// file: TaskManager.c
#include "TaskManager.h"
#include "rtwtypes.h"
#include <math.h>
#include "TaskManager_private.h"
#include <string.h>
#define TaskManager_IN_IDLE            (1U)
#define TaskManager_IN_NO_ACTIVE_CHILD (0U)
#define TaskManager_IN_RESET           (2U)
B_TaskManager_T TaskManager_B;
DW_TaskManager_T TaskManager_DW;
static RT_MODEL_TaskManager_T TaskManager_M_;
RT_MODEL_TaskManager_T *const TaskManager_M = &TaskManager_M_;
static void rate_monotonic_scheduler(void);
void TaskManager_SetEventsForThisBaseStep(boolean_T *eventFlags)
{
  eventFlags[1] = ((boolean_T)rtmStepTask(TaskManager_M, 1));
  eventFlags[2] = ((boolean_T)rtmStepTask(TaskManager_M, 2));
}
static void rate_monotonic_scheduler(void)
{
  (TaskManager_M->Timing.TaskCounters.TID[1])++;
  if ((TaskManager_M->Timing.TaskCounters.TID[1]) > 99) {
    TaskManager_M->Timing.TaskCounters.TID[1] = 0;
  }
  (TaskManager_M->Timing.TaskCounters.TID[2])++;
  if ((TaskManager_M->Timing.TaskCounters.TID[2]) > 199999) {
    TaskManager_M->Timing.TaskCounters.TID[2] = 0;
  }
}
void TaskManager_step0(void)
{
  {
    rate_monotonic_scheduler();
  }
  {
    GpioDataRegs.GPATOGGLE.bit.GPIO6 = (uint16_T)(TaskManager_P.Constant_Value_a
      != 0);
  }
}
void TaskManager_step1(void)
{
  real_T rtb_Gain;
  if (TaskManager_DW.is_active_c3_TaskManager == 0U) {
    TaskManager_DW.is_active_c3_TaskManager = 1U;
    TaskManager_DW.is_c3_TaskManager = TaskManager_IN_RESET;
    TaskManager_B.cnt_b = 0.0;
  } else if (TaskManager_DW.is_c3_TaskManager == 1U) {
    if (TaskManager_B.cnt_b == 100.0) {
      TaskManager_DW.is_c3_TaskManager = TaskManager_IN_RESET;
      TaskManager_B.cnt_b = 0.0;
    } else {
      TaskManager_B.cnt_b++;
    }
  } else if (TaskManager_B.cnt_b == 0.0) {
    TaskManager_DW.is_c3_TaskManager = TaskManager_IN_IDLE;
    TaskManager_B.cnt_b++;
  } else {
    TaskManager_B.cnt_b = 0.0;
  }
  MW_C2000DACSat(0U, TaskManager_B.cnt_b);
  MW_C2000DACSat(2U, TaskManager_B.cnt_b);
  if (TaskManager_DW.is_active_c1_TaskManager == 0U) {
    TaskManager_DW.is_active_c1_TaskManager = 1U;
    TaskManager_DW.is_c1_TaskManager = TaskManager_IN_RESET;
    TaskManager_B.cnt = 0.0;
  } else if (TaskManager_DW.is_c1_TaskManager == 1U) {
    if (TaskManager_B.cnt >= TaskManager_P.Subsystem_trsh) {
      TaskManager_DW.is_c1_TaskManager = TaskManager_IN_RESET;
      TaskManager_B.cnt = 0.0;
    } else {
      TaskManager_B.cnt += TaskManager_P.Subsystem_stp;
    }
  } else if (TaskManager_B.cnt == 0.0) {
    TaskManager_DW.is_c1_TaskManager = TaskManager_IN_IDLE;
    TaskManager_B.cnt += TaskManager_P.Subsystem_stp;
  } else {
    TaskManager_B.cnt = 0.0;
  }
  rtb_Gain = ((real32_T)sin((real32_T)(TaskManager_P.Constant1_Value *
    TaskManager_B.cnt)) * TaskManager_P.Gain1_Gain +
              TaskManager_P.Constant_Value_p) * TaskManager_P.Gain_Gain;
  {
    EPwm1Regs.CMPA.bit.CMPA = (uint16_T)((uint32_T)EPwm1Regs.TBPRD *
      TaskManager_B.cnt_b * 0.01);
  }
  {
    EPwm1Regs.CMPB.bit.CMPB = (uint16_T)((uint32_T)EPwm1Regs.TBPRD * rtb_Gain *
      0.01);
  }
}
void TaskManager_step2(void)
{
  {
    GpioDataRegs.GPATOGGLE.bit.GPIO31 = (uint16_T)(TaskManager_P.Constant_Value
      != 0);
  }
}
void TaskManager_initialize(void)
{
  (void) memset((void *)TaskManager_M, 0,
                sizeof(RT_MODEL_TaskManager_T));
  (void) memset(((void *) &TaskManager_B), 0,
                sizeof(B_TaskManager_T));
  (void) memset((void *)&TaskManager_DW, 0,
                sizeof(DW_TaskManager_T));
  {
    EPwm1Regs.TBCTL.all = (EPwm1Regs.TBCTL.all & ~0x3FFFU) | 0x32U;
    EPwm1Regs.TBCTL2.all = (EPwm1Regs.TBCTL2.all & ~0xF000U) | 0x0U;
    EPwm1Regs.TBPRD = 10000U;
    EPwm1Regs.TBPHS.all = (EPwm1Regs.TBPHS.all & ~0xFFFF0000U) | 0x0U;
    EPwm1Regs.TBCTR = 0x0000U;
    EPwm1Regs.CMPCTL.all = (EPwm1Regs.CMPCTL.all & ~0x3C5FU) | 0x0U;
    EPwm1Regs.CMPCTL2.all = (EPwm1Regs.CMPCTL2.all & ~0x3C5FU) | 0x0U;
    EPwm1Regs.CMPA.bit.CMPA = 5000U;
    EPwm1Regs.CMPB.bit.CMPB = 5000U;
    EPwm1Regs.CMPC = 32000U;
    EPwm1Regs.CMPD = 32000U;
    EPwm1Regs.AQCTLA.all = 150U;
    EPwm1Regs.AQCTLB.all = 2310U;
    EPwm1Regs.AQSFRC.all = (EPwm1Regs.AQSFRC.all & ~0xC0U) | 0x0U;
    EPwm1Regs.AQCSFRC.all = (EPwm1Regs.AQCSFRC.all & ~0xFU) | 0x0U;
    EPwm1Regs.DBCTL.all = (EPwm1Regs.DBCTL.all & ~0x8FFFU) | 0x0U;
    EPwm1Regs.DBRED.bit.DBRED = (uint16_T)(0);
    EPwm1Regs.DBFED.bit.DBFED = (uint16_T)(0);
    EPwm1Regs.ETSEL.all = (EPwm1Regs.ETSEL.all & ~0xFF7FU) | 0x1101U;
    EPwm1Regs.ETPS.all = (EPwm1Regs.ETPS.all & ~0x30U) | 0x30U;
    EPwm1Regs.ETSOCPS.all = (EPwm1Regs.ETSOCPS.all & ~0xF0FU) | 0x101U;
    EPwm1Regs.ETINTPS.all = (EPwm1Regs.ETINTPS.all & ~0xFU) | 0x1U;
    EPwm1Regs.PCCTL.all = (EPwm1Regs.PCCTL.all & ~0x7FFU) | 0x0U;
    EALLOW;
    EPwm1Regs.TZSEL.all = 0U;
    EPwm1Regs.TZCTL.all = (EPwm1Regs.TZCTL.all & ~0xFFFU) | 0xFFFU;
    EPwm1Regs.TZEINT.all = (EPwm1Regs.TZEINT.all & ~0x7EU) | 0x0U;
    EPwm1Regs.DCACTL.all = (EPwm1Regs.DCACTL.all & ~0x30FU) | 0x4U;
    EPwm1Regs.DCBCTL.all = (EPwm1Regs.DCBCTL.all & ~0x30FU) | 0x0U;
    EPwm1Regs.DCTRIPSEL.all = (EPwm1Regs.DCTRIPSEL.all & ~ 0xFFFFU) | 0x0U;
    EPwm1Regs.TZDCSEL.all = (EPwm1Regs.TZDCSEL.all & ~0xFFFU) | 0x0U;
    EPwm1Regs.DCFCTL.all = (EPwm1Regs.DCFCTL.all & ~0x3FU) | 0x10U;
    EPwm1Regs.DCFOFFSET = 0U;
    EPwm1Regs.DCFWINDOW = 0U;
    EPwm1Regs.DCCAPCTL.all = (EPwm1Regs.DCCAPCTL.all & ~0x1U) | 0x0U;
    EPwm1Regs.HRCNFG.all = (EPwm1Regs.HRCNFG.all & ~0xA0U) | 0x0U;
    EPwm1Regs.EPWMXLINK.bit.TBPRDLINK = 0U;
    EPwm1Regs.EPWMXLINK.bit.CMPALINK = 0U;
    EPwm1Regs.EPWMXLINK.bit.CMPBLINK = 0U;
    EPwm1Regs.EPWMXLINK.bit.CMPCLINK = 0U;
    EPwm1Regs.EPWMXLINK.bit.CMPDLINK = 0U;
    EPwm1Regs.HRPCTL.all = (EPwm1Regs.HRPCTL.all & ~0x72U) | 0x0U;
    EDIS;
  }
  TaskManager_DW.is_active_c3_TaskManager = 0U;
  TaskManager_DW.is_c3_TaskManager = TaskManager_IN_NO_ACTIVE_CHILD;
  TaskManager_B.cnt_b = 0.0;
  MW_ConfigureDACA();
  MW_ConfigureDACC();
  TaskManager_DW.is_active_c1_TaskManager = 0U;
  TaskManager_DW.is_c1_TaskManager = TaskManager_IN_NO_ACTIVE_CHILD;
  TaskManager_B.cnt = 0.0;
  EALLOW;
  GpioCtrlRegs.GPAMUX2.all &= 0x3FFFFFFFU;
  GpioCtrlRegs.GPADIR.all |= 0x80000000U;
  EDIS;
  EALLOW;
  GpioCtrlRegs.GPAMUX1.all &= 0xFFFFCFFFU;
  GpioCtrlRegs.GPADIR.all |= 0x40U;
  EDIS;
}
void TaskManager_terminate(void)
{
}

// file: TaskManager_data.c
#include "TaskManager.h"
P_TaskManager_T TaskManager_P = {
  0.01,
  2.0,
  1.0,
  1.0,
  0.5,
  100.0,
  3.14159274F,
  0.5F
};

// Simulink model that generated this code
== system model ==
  Subsystem#1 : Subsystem  <- Trigger: TaskManager
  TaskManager : proctasklib/Task Manager
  Subsystem#2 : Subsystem  <- Trigger: TaskManager/3
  Subsystem#3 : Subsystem  <- Trigger: TaskManager/2
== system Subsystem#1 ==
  TriggerPort#1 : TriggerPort  TriggerType=function-call
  DigitalOutput#1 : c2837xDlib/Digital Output  <- 1: Constant
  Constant : Constant
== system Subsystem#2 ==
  TriggerPort#2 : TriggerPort  TriggerType=function-call
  DAC#1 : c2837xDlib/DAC  <- 1: Stateflowchart#1
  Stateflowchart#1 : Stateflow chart
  DAC#2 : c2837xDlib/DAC  <- 1: Stateflowchart#1
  ePWM#1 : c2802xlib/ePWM  <- 1: Stateflowchart#1, 2: Gain
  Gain : Gain  Gain=100  <- 1: Sum#1
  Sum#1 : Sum  <- 1: Gain1, 2: Constant#1
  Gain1 : Gain  Gain=0.5  <- 1: Trigonometry#1
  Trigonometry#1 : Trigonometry  <- 1: Product#1
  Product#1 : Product  Inputs=**  <- 1: Constant1, 2: Stateflowchart#2
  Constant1 : Constant  Value=pi
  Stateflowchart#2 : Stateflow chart  <- 1: Constant#2, 2: Constant#3
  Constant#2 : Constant  Value=trsh
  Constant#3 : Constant  Value=stp
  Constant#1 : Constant  Value=0.5
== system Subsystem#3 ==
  TriggerPort#3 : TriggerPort  TriggerType=function-call
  DigitalOutput#2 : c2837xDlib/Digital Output  <- 1: Constant#4
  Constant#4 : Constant
== stateflow chart Chart ==
  state RESET
    cnt =0;
  state IDLE
    cnt = cnt + step;
  (default) -> RESET
  RESET -> IDLE : [cnt ==0]
  IDLE -> RESET : [cnt>=treshold]
  data: treshold input; step input; cnt output

== stateflow chart Chart ==
  state RESET
    cnt =0;
  state IDLE
    cnt = cnt + 1;
  (default) -> RESET
  RESET -> IDLE : [cnt ==0]
  IDLE -> RESET : [cnt==100]
  data: cnt output =0
